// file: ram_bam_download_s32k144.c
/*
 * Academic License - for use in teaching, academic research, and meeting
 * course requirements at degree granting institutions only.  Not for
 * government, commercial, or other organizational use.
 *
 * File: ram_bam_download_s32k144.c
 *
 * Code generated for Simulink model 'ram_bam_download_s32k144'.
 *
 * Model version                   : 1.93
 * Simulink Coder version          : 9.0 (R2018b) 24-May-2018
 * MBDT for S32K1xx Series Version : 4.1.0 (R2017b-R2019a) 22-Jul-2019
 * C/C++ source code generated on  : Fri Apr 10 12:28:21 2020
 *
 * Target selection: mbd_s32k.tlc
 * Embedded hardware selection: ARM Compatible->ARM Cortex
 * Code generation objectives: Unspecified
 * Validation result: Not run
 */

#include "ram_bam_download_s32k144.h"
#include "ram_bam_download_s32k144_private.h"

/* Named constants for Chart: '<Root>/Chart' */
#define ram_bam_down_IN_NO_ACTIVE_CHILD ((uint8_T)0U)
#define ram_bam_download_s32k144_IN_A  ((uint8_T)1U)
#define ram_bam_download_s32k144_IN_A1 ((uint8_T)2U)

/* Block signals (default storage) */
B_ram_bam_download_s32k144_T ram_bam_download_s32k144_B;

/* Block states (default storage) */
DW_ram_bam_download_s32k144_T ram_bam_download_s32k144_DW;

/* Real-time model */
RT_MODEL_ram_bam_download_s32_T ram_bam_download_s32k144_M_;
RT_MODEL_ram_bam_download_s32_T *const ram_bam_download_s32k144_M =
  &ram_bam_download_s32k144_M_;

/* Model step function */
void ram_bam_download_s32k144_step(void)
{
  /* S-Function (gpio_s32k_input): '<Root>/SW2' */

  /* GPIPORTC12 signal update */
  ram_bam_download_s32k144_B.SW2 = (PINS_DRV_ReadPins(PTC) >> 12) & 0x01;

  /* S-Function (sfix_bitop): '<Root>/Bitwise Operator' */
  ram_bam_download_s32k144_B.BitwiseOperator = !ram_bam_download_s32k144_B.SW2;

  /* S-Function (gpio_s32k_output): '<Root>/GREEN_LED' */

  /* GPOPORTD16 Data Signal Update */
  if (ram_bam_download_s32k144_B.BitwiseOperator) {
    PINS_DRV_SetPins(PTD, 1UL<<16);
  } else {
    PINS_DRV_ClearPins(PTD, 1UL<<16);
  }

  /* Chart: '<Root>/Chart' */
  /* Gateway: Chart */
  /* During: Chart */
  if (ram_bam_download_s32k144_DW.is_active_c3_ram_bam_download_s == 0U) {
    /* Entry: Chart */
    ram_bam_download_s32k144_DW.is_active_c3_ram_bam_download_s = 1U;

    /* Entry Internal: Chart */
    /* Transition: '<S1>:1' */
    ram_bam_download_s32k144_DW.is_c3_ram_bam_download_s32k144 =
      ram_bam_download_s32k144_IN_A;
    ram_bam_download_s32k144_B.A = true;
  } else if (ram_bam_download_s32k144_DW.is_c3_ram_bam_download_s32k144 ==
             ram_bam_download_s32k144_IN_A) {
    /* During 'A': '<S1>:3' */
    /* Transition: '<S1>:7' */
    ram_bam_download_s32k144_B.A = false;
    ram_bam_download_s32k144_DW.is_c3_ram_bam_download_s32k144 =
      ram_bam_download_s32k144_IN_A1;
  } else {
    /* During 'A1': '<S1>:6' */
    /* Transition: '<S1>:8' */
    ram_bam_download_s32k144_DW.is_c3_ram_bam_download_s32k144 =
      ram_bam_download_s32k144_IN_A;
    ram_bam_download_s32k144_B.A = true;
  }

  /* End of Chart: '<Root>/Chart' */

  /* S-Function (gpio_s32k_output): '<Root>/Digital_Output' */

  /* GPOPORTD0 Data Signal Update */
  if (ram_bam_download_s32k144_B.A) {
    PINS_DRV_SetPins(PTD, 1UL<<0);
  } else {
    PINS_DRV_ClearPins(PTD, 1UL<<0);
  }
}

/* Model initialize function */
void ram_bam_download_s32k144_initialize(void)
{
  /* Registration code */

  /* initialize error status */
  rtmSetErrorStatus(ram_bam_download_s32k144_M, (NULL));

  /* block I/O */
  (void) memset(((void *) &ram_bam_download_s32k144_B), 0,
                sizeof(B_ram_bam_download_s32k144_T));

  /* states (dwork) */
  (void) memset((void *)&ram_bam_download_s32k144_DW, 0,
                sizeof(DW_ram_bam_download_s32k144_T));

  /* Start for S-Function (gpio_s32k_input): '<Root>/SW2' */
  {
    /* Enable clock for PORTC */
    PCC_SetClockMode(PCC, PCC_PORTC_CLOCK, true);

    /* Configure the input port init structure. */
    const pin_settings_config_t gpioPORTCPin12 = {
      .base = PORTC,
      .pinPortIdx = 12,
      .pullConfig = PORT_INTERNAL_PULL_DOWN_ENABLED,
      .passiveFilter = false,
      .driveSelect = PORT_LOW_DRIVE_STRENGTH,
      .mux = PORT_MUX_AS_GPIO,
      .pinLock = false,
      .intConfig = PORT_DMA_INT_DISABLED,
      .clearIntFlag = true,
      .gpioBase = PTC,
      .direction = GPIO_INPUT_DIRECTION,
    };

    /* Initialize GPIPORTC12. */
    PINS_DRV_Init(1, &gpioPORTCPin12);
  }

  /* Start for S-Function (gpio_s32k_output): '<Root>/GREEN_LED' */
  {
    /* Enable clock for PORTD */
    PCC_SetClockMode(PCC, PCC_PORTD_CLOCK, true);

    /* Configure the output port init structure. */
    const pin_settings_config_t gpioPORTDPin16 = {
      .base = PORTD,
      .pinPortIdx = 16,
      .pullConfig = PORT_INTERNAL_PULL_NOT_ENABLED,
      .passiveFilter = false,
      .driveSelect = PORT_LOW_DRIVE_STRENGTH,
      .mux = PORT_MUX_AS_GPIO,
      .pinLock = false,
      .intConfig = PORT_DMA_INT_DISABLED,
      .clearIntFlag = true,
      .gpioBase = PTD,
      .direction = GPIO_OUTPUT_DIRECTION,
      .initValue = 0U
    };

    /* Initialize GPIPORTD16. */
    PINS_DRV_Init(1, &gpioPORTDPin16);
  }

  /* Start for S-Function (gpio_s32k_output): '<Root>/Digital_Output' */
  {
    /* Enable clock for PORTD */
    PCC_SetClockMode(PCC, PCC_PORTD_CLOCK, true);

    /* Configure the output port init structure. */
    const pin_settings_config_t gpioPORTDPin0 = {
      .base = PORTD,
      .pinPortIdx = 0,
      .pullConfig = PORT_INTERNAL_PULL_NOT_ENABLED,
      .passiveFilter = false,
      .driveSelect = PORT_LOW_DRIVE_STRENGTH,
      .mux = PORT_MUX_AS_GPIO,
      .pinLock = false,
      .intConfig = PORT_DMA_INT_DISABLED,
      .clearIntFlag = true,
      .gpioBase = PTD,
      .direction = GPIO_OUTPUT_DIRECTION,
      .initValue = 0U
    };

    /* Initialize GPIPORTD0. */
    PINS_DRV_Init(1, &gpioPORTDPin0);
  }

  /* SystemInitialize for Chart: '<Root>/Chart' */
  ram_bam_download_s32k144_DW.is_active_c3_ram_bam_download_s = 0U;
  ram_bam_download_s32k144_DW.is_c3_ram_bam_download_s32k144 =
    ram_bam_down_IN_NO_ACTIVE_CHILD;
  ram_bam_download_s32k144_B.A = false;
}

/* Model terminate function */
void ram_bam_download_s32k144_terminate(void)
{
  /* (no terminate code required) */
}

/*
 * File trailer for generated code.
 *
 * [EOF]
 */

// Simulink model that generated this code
simulink model "ram_bam_download_s32k144"  (Simulink 9.2)
settings: Solver=FixedStepDiscrete  StartTime=0.0  StopTime=10.0  FixedStep=0.1  RelTol=1e-3  EnableMultiTasking=on
InitFcn:
  | mbd_s32k_consistency_checks(bdroot(gcs));
undefined symbols (not defined in the file): LQFP
libraries: mbd_s32k1xx_ec_toolbox x4, simulink x2

== system ram_bam_download_s32k144 ==
  Bitwise Operator : simulink/Logic and Bit Operations/Bitwise Operator  logicop=NOT  UseBitMask=off  BitMask=bin2dec('11011001')  BitMaskRealWorld=Stored Integer
  Chart : Stateflow chart  TreatAsAtomicUnit=on
  Digital_Output : mbd_s32k1xx_ec_toolbox/GPIO Blocks/Digital_Output  gpio_pin=PTD0: [PTD0 | Port D I/O]  init_val=Low  drive_strength=Low
  GREEN_LED : mbd_s32k1xx_ec_toolbox/GPIO Blocks/Digital_Output  gpio_pin=PTD16: [PTD16 | Port D I/O]  init_val=Low  drive_strength=Low
  MBD_S32K14x_Config_Information : mbd_s32k1xx_ec_toolbox/MBD_S32K1xx_Config_Information  mbdt_ver=0  disp_str=|  config_params=[]  mcu_target_name=S32K144  mcu_target_package=100-LQFP  mcu_target_sram_size=64KB  mcu_system_clock_freq=80  mcu_xtal_freq=External 8  mcu_steptick_timer=LPIT Channel 0  mcu_steptick_prio=15  ds_import_enable=on  target_compiler=GCC  target_memory=SRAM  gcc_target_compile_opts=-mcpu=cortex-m4 -mthumb -mfloat-abi=hard -mfpu=fpv4-sp-d16 -O1 -g -gstrict-dwarf  gcc_target_assemble_opts=-mcpu=cortex-m4 -mthumb -mfloat-abi=hard -mfpu=fpv4-sp-d16 -g  gcc_target_link_opts=-mcpu=cortex-m4 -mthumb -mfloat-abi=hard -mfpu=fpv4-sp-d16  gcc_target_default_lcf=on  gcc_target_user_lcf=S32K144_64_ram.ld  ghs_target_compile_opts=-cpu=cortexm4f -thumb -DARM_MATH_CM4 -fpu=vfpv4_d16 -fsingle -Ogeneral -Wundef -Wimplicit-int -Wshadow -Wtrigraphs --no_commons --gnu_asm -gnu99 -gdwarf-2 -G  ghs_target_assemble_opts=-cpu=cortexm4f -fpu=vfpv4_d16  ghs_target_link_opts=-cpu=cortexm4f -thumb -fpu=vfpv4_d16  ghs_target_default_lcf=on  ghs_target_user_lcf=S32K144_64_ram.ld  iar_target_compile_opts=--cpu=Cortex-M4F --thumb --fpu=VFPv4_sp -Ol -e --debug --dlib_config normal  iar_target_assemble_opts=--cpu Cortex-M4F --thumb --fpu VFPv4_sp  iar_target_link_opts=--no_exceptions --vfe --inline  iar_target_default_lcf=on  iar_target_user_lcf=S32K144_64_ram.icf  pil_download_enable=off  rbl_download_enable=on  rbl_start_delay=5000000  rbl_download_interface=Serial  rbl_restart_request=on  rbl_com_port=Custom  rbl_com_port_custom=COM1  pil_download_rate=115200  pil_opensda_drive=Custom  pil_opensda_drive_custom=D  pil_uart_instance=0  pil_uart_rx=PTA2: [LPUART0_RX | Receive]  pil_uart_tx=PTA3: [LPUART0_TX | Transmit]  FTM_PWM_PcrCheckEnDis=on  FTM_Input_Edge_Inputs_PcrCheckEnDis=on  FTM_Dual_Edge_Inputs_PcrCheckEnDis=on  FTM_Quadrature_Inputs_PcrCheckEnDis=on  FTM_Hall_Sensor_Inputs_PcrCheckEnDis=on  LPTMR_PcrCheckEnDis=on  PIT_PcrCheckEnDis=on  RTC_PcrCheckEnDis=on  FlexCAN_PcrCheckEnDis=on  LIN_PcrCheckEnDis=on  FlexIO_PcrCheckEnDis=on  LPI2C_PcrCheckEnDis=on  LPSPI_PcrCheckEnDis=on  LPUART_PcrCheckEnDis=on  CMP_PcrCheckEnDis=on  GPIO_OutputPcrCheckEnDis=on  GPIO_InputPcrCheckEnDis=on  SBC_PcrCheckEnDis=on  AMMCLIB_PcrCheckEnDis=on  FM_PcrCheckEnDis=on  Profile_PcrCheckEnDis=on  ConfigParams_PcrCheckEnDis=on  ModelRef_PcrCheckEnDis=on  PDB0_PcrCheckEnDis=on  CSEc_PcrCheckEnDis=on  eDMA_PcrCheckEnDis=on  ADC_PcrCheckEnDis=on  WDOG_PcrCheckEnDis=on
      | Target : S32K144-64KB_SRAM
      | Package : 100-pin
      | System clock : 80 MHz
      | XTAL clock : External 8 MHz
      | Compiler : IAR
      | Target Type : FLASH
      | Download Code after build : off
      | Step Tick Interrupt Priority : 15
  Model Info : simulink/Model-Wide Utilities/Model Info  Frame=off  DisplayStringWithTags=|  HorizontalTextAlignment=Left  LeftAlignmentValue=0.02
      | Model Name: %<ModelName>
      | 
      | Description: %<Description>
  SW2 : mbd_s32k1xx_ec_toolbox/GPIO Blocks/Digital_Input  gpio_pin=PTC12: [PTC12 | Port C I/O]  pull_resistor=Pulldown  passive_filter=off
  wires:
  Chart/1(" A") -> Digital_Output/1
  SW2/1 -> Bitwise Operator/1
  Bitwise Operator/1 -> GREEN_LED/1

== stateflow chart Chart ==
  state A
  state A1
  (default) -> A
  A -> A1
  A1 -> A
  data: A output boolean [0..1]
